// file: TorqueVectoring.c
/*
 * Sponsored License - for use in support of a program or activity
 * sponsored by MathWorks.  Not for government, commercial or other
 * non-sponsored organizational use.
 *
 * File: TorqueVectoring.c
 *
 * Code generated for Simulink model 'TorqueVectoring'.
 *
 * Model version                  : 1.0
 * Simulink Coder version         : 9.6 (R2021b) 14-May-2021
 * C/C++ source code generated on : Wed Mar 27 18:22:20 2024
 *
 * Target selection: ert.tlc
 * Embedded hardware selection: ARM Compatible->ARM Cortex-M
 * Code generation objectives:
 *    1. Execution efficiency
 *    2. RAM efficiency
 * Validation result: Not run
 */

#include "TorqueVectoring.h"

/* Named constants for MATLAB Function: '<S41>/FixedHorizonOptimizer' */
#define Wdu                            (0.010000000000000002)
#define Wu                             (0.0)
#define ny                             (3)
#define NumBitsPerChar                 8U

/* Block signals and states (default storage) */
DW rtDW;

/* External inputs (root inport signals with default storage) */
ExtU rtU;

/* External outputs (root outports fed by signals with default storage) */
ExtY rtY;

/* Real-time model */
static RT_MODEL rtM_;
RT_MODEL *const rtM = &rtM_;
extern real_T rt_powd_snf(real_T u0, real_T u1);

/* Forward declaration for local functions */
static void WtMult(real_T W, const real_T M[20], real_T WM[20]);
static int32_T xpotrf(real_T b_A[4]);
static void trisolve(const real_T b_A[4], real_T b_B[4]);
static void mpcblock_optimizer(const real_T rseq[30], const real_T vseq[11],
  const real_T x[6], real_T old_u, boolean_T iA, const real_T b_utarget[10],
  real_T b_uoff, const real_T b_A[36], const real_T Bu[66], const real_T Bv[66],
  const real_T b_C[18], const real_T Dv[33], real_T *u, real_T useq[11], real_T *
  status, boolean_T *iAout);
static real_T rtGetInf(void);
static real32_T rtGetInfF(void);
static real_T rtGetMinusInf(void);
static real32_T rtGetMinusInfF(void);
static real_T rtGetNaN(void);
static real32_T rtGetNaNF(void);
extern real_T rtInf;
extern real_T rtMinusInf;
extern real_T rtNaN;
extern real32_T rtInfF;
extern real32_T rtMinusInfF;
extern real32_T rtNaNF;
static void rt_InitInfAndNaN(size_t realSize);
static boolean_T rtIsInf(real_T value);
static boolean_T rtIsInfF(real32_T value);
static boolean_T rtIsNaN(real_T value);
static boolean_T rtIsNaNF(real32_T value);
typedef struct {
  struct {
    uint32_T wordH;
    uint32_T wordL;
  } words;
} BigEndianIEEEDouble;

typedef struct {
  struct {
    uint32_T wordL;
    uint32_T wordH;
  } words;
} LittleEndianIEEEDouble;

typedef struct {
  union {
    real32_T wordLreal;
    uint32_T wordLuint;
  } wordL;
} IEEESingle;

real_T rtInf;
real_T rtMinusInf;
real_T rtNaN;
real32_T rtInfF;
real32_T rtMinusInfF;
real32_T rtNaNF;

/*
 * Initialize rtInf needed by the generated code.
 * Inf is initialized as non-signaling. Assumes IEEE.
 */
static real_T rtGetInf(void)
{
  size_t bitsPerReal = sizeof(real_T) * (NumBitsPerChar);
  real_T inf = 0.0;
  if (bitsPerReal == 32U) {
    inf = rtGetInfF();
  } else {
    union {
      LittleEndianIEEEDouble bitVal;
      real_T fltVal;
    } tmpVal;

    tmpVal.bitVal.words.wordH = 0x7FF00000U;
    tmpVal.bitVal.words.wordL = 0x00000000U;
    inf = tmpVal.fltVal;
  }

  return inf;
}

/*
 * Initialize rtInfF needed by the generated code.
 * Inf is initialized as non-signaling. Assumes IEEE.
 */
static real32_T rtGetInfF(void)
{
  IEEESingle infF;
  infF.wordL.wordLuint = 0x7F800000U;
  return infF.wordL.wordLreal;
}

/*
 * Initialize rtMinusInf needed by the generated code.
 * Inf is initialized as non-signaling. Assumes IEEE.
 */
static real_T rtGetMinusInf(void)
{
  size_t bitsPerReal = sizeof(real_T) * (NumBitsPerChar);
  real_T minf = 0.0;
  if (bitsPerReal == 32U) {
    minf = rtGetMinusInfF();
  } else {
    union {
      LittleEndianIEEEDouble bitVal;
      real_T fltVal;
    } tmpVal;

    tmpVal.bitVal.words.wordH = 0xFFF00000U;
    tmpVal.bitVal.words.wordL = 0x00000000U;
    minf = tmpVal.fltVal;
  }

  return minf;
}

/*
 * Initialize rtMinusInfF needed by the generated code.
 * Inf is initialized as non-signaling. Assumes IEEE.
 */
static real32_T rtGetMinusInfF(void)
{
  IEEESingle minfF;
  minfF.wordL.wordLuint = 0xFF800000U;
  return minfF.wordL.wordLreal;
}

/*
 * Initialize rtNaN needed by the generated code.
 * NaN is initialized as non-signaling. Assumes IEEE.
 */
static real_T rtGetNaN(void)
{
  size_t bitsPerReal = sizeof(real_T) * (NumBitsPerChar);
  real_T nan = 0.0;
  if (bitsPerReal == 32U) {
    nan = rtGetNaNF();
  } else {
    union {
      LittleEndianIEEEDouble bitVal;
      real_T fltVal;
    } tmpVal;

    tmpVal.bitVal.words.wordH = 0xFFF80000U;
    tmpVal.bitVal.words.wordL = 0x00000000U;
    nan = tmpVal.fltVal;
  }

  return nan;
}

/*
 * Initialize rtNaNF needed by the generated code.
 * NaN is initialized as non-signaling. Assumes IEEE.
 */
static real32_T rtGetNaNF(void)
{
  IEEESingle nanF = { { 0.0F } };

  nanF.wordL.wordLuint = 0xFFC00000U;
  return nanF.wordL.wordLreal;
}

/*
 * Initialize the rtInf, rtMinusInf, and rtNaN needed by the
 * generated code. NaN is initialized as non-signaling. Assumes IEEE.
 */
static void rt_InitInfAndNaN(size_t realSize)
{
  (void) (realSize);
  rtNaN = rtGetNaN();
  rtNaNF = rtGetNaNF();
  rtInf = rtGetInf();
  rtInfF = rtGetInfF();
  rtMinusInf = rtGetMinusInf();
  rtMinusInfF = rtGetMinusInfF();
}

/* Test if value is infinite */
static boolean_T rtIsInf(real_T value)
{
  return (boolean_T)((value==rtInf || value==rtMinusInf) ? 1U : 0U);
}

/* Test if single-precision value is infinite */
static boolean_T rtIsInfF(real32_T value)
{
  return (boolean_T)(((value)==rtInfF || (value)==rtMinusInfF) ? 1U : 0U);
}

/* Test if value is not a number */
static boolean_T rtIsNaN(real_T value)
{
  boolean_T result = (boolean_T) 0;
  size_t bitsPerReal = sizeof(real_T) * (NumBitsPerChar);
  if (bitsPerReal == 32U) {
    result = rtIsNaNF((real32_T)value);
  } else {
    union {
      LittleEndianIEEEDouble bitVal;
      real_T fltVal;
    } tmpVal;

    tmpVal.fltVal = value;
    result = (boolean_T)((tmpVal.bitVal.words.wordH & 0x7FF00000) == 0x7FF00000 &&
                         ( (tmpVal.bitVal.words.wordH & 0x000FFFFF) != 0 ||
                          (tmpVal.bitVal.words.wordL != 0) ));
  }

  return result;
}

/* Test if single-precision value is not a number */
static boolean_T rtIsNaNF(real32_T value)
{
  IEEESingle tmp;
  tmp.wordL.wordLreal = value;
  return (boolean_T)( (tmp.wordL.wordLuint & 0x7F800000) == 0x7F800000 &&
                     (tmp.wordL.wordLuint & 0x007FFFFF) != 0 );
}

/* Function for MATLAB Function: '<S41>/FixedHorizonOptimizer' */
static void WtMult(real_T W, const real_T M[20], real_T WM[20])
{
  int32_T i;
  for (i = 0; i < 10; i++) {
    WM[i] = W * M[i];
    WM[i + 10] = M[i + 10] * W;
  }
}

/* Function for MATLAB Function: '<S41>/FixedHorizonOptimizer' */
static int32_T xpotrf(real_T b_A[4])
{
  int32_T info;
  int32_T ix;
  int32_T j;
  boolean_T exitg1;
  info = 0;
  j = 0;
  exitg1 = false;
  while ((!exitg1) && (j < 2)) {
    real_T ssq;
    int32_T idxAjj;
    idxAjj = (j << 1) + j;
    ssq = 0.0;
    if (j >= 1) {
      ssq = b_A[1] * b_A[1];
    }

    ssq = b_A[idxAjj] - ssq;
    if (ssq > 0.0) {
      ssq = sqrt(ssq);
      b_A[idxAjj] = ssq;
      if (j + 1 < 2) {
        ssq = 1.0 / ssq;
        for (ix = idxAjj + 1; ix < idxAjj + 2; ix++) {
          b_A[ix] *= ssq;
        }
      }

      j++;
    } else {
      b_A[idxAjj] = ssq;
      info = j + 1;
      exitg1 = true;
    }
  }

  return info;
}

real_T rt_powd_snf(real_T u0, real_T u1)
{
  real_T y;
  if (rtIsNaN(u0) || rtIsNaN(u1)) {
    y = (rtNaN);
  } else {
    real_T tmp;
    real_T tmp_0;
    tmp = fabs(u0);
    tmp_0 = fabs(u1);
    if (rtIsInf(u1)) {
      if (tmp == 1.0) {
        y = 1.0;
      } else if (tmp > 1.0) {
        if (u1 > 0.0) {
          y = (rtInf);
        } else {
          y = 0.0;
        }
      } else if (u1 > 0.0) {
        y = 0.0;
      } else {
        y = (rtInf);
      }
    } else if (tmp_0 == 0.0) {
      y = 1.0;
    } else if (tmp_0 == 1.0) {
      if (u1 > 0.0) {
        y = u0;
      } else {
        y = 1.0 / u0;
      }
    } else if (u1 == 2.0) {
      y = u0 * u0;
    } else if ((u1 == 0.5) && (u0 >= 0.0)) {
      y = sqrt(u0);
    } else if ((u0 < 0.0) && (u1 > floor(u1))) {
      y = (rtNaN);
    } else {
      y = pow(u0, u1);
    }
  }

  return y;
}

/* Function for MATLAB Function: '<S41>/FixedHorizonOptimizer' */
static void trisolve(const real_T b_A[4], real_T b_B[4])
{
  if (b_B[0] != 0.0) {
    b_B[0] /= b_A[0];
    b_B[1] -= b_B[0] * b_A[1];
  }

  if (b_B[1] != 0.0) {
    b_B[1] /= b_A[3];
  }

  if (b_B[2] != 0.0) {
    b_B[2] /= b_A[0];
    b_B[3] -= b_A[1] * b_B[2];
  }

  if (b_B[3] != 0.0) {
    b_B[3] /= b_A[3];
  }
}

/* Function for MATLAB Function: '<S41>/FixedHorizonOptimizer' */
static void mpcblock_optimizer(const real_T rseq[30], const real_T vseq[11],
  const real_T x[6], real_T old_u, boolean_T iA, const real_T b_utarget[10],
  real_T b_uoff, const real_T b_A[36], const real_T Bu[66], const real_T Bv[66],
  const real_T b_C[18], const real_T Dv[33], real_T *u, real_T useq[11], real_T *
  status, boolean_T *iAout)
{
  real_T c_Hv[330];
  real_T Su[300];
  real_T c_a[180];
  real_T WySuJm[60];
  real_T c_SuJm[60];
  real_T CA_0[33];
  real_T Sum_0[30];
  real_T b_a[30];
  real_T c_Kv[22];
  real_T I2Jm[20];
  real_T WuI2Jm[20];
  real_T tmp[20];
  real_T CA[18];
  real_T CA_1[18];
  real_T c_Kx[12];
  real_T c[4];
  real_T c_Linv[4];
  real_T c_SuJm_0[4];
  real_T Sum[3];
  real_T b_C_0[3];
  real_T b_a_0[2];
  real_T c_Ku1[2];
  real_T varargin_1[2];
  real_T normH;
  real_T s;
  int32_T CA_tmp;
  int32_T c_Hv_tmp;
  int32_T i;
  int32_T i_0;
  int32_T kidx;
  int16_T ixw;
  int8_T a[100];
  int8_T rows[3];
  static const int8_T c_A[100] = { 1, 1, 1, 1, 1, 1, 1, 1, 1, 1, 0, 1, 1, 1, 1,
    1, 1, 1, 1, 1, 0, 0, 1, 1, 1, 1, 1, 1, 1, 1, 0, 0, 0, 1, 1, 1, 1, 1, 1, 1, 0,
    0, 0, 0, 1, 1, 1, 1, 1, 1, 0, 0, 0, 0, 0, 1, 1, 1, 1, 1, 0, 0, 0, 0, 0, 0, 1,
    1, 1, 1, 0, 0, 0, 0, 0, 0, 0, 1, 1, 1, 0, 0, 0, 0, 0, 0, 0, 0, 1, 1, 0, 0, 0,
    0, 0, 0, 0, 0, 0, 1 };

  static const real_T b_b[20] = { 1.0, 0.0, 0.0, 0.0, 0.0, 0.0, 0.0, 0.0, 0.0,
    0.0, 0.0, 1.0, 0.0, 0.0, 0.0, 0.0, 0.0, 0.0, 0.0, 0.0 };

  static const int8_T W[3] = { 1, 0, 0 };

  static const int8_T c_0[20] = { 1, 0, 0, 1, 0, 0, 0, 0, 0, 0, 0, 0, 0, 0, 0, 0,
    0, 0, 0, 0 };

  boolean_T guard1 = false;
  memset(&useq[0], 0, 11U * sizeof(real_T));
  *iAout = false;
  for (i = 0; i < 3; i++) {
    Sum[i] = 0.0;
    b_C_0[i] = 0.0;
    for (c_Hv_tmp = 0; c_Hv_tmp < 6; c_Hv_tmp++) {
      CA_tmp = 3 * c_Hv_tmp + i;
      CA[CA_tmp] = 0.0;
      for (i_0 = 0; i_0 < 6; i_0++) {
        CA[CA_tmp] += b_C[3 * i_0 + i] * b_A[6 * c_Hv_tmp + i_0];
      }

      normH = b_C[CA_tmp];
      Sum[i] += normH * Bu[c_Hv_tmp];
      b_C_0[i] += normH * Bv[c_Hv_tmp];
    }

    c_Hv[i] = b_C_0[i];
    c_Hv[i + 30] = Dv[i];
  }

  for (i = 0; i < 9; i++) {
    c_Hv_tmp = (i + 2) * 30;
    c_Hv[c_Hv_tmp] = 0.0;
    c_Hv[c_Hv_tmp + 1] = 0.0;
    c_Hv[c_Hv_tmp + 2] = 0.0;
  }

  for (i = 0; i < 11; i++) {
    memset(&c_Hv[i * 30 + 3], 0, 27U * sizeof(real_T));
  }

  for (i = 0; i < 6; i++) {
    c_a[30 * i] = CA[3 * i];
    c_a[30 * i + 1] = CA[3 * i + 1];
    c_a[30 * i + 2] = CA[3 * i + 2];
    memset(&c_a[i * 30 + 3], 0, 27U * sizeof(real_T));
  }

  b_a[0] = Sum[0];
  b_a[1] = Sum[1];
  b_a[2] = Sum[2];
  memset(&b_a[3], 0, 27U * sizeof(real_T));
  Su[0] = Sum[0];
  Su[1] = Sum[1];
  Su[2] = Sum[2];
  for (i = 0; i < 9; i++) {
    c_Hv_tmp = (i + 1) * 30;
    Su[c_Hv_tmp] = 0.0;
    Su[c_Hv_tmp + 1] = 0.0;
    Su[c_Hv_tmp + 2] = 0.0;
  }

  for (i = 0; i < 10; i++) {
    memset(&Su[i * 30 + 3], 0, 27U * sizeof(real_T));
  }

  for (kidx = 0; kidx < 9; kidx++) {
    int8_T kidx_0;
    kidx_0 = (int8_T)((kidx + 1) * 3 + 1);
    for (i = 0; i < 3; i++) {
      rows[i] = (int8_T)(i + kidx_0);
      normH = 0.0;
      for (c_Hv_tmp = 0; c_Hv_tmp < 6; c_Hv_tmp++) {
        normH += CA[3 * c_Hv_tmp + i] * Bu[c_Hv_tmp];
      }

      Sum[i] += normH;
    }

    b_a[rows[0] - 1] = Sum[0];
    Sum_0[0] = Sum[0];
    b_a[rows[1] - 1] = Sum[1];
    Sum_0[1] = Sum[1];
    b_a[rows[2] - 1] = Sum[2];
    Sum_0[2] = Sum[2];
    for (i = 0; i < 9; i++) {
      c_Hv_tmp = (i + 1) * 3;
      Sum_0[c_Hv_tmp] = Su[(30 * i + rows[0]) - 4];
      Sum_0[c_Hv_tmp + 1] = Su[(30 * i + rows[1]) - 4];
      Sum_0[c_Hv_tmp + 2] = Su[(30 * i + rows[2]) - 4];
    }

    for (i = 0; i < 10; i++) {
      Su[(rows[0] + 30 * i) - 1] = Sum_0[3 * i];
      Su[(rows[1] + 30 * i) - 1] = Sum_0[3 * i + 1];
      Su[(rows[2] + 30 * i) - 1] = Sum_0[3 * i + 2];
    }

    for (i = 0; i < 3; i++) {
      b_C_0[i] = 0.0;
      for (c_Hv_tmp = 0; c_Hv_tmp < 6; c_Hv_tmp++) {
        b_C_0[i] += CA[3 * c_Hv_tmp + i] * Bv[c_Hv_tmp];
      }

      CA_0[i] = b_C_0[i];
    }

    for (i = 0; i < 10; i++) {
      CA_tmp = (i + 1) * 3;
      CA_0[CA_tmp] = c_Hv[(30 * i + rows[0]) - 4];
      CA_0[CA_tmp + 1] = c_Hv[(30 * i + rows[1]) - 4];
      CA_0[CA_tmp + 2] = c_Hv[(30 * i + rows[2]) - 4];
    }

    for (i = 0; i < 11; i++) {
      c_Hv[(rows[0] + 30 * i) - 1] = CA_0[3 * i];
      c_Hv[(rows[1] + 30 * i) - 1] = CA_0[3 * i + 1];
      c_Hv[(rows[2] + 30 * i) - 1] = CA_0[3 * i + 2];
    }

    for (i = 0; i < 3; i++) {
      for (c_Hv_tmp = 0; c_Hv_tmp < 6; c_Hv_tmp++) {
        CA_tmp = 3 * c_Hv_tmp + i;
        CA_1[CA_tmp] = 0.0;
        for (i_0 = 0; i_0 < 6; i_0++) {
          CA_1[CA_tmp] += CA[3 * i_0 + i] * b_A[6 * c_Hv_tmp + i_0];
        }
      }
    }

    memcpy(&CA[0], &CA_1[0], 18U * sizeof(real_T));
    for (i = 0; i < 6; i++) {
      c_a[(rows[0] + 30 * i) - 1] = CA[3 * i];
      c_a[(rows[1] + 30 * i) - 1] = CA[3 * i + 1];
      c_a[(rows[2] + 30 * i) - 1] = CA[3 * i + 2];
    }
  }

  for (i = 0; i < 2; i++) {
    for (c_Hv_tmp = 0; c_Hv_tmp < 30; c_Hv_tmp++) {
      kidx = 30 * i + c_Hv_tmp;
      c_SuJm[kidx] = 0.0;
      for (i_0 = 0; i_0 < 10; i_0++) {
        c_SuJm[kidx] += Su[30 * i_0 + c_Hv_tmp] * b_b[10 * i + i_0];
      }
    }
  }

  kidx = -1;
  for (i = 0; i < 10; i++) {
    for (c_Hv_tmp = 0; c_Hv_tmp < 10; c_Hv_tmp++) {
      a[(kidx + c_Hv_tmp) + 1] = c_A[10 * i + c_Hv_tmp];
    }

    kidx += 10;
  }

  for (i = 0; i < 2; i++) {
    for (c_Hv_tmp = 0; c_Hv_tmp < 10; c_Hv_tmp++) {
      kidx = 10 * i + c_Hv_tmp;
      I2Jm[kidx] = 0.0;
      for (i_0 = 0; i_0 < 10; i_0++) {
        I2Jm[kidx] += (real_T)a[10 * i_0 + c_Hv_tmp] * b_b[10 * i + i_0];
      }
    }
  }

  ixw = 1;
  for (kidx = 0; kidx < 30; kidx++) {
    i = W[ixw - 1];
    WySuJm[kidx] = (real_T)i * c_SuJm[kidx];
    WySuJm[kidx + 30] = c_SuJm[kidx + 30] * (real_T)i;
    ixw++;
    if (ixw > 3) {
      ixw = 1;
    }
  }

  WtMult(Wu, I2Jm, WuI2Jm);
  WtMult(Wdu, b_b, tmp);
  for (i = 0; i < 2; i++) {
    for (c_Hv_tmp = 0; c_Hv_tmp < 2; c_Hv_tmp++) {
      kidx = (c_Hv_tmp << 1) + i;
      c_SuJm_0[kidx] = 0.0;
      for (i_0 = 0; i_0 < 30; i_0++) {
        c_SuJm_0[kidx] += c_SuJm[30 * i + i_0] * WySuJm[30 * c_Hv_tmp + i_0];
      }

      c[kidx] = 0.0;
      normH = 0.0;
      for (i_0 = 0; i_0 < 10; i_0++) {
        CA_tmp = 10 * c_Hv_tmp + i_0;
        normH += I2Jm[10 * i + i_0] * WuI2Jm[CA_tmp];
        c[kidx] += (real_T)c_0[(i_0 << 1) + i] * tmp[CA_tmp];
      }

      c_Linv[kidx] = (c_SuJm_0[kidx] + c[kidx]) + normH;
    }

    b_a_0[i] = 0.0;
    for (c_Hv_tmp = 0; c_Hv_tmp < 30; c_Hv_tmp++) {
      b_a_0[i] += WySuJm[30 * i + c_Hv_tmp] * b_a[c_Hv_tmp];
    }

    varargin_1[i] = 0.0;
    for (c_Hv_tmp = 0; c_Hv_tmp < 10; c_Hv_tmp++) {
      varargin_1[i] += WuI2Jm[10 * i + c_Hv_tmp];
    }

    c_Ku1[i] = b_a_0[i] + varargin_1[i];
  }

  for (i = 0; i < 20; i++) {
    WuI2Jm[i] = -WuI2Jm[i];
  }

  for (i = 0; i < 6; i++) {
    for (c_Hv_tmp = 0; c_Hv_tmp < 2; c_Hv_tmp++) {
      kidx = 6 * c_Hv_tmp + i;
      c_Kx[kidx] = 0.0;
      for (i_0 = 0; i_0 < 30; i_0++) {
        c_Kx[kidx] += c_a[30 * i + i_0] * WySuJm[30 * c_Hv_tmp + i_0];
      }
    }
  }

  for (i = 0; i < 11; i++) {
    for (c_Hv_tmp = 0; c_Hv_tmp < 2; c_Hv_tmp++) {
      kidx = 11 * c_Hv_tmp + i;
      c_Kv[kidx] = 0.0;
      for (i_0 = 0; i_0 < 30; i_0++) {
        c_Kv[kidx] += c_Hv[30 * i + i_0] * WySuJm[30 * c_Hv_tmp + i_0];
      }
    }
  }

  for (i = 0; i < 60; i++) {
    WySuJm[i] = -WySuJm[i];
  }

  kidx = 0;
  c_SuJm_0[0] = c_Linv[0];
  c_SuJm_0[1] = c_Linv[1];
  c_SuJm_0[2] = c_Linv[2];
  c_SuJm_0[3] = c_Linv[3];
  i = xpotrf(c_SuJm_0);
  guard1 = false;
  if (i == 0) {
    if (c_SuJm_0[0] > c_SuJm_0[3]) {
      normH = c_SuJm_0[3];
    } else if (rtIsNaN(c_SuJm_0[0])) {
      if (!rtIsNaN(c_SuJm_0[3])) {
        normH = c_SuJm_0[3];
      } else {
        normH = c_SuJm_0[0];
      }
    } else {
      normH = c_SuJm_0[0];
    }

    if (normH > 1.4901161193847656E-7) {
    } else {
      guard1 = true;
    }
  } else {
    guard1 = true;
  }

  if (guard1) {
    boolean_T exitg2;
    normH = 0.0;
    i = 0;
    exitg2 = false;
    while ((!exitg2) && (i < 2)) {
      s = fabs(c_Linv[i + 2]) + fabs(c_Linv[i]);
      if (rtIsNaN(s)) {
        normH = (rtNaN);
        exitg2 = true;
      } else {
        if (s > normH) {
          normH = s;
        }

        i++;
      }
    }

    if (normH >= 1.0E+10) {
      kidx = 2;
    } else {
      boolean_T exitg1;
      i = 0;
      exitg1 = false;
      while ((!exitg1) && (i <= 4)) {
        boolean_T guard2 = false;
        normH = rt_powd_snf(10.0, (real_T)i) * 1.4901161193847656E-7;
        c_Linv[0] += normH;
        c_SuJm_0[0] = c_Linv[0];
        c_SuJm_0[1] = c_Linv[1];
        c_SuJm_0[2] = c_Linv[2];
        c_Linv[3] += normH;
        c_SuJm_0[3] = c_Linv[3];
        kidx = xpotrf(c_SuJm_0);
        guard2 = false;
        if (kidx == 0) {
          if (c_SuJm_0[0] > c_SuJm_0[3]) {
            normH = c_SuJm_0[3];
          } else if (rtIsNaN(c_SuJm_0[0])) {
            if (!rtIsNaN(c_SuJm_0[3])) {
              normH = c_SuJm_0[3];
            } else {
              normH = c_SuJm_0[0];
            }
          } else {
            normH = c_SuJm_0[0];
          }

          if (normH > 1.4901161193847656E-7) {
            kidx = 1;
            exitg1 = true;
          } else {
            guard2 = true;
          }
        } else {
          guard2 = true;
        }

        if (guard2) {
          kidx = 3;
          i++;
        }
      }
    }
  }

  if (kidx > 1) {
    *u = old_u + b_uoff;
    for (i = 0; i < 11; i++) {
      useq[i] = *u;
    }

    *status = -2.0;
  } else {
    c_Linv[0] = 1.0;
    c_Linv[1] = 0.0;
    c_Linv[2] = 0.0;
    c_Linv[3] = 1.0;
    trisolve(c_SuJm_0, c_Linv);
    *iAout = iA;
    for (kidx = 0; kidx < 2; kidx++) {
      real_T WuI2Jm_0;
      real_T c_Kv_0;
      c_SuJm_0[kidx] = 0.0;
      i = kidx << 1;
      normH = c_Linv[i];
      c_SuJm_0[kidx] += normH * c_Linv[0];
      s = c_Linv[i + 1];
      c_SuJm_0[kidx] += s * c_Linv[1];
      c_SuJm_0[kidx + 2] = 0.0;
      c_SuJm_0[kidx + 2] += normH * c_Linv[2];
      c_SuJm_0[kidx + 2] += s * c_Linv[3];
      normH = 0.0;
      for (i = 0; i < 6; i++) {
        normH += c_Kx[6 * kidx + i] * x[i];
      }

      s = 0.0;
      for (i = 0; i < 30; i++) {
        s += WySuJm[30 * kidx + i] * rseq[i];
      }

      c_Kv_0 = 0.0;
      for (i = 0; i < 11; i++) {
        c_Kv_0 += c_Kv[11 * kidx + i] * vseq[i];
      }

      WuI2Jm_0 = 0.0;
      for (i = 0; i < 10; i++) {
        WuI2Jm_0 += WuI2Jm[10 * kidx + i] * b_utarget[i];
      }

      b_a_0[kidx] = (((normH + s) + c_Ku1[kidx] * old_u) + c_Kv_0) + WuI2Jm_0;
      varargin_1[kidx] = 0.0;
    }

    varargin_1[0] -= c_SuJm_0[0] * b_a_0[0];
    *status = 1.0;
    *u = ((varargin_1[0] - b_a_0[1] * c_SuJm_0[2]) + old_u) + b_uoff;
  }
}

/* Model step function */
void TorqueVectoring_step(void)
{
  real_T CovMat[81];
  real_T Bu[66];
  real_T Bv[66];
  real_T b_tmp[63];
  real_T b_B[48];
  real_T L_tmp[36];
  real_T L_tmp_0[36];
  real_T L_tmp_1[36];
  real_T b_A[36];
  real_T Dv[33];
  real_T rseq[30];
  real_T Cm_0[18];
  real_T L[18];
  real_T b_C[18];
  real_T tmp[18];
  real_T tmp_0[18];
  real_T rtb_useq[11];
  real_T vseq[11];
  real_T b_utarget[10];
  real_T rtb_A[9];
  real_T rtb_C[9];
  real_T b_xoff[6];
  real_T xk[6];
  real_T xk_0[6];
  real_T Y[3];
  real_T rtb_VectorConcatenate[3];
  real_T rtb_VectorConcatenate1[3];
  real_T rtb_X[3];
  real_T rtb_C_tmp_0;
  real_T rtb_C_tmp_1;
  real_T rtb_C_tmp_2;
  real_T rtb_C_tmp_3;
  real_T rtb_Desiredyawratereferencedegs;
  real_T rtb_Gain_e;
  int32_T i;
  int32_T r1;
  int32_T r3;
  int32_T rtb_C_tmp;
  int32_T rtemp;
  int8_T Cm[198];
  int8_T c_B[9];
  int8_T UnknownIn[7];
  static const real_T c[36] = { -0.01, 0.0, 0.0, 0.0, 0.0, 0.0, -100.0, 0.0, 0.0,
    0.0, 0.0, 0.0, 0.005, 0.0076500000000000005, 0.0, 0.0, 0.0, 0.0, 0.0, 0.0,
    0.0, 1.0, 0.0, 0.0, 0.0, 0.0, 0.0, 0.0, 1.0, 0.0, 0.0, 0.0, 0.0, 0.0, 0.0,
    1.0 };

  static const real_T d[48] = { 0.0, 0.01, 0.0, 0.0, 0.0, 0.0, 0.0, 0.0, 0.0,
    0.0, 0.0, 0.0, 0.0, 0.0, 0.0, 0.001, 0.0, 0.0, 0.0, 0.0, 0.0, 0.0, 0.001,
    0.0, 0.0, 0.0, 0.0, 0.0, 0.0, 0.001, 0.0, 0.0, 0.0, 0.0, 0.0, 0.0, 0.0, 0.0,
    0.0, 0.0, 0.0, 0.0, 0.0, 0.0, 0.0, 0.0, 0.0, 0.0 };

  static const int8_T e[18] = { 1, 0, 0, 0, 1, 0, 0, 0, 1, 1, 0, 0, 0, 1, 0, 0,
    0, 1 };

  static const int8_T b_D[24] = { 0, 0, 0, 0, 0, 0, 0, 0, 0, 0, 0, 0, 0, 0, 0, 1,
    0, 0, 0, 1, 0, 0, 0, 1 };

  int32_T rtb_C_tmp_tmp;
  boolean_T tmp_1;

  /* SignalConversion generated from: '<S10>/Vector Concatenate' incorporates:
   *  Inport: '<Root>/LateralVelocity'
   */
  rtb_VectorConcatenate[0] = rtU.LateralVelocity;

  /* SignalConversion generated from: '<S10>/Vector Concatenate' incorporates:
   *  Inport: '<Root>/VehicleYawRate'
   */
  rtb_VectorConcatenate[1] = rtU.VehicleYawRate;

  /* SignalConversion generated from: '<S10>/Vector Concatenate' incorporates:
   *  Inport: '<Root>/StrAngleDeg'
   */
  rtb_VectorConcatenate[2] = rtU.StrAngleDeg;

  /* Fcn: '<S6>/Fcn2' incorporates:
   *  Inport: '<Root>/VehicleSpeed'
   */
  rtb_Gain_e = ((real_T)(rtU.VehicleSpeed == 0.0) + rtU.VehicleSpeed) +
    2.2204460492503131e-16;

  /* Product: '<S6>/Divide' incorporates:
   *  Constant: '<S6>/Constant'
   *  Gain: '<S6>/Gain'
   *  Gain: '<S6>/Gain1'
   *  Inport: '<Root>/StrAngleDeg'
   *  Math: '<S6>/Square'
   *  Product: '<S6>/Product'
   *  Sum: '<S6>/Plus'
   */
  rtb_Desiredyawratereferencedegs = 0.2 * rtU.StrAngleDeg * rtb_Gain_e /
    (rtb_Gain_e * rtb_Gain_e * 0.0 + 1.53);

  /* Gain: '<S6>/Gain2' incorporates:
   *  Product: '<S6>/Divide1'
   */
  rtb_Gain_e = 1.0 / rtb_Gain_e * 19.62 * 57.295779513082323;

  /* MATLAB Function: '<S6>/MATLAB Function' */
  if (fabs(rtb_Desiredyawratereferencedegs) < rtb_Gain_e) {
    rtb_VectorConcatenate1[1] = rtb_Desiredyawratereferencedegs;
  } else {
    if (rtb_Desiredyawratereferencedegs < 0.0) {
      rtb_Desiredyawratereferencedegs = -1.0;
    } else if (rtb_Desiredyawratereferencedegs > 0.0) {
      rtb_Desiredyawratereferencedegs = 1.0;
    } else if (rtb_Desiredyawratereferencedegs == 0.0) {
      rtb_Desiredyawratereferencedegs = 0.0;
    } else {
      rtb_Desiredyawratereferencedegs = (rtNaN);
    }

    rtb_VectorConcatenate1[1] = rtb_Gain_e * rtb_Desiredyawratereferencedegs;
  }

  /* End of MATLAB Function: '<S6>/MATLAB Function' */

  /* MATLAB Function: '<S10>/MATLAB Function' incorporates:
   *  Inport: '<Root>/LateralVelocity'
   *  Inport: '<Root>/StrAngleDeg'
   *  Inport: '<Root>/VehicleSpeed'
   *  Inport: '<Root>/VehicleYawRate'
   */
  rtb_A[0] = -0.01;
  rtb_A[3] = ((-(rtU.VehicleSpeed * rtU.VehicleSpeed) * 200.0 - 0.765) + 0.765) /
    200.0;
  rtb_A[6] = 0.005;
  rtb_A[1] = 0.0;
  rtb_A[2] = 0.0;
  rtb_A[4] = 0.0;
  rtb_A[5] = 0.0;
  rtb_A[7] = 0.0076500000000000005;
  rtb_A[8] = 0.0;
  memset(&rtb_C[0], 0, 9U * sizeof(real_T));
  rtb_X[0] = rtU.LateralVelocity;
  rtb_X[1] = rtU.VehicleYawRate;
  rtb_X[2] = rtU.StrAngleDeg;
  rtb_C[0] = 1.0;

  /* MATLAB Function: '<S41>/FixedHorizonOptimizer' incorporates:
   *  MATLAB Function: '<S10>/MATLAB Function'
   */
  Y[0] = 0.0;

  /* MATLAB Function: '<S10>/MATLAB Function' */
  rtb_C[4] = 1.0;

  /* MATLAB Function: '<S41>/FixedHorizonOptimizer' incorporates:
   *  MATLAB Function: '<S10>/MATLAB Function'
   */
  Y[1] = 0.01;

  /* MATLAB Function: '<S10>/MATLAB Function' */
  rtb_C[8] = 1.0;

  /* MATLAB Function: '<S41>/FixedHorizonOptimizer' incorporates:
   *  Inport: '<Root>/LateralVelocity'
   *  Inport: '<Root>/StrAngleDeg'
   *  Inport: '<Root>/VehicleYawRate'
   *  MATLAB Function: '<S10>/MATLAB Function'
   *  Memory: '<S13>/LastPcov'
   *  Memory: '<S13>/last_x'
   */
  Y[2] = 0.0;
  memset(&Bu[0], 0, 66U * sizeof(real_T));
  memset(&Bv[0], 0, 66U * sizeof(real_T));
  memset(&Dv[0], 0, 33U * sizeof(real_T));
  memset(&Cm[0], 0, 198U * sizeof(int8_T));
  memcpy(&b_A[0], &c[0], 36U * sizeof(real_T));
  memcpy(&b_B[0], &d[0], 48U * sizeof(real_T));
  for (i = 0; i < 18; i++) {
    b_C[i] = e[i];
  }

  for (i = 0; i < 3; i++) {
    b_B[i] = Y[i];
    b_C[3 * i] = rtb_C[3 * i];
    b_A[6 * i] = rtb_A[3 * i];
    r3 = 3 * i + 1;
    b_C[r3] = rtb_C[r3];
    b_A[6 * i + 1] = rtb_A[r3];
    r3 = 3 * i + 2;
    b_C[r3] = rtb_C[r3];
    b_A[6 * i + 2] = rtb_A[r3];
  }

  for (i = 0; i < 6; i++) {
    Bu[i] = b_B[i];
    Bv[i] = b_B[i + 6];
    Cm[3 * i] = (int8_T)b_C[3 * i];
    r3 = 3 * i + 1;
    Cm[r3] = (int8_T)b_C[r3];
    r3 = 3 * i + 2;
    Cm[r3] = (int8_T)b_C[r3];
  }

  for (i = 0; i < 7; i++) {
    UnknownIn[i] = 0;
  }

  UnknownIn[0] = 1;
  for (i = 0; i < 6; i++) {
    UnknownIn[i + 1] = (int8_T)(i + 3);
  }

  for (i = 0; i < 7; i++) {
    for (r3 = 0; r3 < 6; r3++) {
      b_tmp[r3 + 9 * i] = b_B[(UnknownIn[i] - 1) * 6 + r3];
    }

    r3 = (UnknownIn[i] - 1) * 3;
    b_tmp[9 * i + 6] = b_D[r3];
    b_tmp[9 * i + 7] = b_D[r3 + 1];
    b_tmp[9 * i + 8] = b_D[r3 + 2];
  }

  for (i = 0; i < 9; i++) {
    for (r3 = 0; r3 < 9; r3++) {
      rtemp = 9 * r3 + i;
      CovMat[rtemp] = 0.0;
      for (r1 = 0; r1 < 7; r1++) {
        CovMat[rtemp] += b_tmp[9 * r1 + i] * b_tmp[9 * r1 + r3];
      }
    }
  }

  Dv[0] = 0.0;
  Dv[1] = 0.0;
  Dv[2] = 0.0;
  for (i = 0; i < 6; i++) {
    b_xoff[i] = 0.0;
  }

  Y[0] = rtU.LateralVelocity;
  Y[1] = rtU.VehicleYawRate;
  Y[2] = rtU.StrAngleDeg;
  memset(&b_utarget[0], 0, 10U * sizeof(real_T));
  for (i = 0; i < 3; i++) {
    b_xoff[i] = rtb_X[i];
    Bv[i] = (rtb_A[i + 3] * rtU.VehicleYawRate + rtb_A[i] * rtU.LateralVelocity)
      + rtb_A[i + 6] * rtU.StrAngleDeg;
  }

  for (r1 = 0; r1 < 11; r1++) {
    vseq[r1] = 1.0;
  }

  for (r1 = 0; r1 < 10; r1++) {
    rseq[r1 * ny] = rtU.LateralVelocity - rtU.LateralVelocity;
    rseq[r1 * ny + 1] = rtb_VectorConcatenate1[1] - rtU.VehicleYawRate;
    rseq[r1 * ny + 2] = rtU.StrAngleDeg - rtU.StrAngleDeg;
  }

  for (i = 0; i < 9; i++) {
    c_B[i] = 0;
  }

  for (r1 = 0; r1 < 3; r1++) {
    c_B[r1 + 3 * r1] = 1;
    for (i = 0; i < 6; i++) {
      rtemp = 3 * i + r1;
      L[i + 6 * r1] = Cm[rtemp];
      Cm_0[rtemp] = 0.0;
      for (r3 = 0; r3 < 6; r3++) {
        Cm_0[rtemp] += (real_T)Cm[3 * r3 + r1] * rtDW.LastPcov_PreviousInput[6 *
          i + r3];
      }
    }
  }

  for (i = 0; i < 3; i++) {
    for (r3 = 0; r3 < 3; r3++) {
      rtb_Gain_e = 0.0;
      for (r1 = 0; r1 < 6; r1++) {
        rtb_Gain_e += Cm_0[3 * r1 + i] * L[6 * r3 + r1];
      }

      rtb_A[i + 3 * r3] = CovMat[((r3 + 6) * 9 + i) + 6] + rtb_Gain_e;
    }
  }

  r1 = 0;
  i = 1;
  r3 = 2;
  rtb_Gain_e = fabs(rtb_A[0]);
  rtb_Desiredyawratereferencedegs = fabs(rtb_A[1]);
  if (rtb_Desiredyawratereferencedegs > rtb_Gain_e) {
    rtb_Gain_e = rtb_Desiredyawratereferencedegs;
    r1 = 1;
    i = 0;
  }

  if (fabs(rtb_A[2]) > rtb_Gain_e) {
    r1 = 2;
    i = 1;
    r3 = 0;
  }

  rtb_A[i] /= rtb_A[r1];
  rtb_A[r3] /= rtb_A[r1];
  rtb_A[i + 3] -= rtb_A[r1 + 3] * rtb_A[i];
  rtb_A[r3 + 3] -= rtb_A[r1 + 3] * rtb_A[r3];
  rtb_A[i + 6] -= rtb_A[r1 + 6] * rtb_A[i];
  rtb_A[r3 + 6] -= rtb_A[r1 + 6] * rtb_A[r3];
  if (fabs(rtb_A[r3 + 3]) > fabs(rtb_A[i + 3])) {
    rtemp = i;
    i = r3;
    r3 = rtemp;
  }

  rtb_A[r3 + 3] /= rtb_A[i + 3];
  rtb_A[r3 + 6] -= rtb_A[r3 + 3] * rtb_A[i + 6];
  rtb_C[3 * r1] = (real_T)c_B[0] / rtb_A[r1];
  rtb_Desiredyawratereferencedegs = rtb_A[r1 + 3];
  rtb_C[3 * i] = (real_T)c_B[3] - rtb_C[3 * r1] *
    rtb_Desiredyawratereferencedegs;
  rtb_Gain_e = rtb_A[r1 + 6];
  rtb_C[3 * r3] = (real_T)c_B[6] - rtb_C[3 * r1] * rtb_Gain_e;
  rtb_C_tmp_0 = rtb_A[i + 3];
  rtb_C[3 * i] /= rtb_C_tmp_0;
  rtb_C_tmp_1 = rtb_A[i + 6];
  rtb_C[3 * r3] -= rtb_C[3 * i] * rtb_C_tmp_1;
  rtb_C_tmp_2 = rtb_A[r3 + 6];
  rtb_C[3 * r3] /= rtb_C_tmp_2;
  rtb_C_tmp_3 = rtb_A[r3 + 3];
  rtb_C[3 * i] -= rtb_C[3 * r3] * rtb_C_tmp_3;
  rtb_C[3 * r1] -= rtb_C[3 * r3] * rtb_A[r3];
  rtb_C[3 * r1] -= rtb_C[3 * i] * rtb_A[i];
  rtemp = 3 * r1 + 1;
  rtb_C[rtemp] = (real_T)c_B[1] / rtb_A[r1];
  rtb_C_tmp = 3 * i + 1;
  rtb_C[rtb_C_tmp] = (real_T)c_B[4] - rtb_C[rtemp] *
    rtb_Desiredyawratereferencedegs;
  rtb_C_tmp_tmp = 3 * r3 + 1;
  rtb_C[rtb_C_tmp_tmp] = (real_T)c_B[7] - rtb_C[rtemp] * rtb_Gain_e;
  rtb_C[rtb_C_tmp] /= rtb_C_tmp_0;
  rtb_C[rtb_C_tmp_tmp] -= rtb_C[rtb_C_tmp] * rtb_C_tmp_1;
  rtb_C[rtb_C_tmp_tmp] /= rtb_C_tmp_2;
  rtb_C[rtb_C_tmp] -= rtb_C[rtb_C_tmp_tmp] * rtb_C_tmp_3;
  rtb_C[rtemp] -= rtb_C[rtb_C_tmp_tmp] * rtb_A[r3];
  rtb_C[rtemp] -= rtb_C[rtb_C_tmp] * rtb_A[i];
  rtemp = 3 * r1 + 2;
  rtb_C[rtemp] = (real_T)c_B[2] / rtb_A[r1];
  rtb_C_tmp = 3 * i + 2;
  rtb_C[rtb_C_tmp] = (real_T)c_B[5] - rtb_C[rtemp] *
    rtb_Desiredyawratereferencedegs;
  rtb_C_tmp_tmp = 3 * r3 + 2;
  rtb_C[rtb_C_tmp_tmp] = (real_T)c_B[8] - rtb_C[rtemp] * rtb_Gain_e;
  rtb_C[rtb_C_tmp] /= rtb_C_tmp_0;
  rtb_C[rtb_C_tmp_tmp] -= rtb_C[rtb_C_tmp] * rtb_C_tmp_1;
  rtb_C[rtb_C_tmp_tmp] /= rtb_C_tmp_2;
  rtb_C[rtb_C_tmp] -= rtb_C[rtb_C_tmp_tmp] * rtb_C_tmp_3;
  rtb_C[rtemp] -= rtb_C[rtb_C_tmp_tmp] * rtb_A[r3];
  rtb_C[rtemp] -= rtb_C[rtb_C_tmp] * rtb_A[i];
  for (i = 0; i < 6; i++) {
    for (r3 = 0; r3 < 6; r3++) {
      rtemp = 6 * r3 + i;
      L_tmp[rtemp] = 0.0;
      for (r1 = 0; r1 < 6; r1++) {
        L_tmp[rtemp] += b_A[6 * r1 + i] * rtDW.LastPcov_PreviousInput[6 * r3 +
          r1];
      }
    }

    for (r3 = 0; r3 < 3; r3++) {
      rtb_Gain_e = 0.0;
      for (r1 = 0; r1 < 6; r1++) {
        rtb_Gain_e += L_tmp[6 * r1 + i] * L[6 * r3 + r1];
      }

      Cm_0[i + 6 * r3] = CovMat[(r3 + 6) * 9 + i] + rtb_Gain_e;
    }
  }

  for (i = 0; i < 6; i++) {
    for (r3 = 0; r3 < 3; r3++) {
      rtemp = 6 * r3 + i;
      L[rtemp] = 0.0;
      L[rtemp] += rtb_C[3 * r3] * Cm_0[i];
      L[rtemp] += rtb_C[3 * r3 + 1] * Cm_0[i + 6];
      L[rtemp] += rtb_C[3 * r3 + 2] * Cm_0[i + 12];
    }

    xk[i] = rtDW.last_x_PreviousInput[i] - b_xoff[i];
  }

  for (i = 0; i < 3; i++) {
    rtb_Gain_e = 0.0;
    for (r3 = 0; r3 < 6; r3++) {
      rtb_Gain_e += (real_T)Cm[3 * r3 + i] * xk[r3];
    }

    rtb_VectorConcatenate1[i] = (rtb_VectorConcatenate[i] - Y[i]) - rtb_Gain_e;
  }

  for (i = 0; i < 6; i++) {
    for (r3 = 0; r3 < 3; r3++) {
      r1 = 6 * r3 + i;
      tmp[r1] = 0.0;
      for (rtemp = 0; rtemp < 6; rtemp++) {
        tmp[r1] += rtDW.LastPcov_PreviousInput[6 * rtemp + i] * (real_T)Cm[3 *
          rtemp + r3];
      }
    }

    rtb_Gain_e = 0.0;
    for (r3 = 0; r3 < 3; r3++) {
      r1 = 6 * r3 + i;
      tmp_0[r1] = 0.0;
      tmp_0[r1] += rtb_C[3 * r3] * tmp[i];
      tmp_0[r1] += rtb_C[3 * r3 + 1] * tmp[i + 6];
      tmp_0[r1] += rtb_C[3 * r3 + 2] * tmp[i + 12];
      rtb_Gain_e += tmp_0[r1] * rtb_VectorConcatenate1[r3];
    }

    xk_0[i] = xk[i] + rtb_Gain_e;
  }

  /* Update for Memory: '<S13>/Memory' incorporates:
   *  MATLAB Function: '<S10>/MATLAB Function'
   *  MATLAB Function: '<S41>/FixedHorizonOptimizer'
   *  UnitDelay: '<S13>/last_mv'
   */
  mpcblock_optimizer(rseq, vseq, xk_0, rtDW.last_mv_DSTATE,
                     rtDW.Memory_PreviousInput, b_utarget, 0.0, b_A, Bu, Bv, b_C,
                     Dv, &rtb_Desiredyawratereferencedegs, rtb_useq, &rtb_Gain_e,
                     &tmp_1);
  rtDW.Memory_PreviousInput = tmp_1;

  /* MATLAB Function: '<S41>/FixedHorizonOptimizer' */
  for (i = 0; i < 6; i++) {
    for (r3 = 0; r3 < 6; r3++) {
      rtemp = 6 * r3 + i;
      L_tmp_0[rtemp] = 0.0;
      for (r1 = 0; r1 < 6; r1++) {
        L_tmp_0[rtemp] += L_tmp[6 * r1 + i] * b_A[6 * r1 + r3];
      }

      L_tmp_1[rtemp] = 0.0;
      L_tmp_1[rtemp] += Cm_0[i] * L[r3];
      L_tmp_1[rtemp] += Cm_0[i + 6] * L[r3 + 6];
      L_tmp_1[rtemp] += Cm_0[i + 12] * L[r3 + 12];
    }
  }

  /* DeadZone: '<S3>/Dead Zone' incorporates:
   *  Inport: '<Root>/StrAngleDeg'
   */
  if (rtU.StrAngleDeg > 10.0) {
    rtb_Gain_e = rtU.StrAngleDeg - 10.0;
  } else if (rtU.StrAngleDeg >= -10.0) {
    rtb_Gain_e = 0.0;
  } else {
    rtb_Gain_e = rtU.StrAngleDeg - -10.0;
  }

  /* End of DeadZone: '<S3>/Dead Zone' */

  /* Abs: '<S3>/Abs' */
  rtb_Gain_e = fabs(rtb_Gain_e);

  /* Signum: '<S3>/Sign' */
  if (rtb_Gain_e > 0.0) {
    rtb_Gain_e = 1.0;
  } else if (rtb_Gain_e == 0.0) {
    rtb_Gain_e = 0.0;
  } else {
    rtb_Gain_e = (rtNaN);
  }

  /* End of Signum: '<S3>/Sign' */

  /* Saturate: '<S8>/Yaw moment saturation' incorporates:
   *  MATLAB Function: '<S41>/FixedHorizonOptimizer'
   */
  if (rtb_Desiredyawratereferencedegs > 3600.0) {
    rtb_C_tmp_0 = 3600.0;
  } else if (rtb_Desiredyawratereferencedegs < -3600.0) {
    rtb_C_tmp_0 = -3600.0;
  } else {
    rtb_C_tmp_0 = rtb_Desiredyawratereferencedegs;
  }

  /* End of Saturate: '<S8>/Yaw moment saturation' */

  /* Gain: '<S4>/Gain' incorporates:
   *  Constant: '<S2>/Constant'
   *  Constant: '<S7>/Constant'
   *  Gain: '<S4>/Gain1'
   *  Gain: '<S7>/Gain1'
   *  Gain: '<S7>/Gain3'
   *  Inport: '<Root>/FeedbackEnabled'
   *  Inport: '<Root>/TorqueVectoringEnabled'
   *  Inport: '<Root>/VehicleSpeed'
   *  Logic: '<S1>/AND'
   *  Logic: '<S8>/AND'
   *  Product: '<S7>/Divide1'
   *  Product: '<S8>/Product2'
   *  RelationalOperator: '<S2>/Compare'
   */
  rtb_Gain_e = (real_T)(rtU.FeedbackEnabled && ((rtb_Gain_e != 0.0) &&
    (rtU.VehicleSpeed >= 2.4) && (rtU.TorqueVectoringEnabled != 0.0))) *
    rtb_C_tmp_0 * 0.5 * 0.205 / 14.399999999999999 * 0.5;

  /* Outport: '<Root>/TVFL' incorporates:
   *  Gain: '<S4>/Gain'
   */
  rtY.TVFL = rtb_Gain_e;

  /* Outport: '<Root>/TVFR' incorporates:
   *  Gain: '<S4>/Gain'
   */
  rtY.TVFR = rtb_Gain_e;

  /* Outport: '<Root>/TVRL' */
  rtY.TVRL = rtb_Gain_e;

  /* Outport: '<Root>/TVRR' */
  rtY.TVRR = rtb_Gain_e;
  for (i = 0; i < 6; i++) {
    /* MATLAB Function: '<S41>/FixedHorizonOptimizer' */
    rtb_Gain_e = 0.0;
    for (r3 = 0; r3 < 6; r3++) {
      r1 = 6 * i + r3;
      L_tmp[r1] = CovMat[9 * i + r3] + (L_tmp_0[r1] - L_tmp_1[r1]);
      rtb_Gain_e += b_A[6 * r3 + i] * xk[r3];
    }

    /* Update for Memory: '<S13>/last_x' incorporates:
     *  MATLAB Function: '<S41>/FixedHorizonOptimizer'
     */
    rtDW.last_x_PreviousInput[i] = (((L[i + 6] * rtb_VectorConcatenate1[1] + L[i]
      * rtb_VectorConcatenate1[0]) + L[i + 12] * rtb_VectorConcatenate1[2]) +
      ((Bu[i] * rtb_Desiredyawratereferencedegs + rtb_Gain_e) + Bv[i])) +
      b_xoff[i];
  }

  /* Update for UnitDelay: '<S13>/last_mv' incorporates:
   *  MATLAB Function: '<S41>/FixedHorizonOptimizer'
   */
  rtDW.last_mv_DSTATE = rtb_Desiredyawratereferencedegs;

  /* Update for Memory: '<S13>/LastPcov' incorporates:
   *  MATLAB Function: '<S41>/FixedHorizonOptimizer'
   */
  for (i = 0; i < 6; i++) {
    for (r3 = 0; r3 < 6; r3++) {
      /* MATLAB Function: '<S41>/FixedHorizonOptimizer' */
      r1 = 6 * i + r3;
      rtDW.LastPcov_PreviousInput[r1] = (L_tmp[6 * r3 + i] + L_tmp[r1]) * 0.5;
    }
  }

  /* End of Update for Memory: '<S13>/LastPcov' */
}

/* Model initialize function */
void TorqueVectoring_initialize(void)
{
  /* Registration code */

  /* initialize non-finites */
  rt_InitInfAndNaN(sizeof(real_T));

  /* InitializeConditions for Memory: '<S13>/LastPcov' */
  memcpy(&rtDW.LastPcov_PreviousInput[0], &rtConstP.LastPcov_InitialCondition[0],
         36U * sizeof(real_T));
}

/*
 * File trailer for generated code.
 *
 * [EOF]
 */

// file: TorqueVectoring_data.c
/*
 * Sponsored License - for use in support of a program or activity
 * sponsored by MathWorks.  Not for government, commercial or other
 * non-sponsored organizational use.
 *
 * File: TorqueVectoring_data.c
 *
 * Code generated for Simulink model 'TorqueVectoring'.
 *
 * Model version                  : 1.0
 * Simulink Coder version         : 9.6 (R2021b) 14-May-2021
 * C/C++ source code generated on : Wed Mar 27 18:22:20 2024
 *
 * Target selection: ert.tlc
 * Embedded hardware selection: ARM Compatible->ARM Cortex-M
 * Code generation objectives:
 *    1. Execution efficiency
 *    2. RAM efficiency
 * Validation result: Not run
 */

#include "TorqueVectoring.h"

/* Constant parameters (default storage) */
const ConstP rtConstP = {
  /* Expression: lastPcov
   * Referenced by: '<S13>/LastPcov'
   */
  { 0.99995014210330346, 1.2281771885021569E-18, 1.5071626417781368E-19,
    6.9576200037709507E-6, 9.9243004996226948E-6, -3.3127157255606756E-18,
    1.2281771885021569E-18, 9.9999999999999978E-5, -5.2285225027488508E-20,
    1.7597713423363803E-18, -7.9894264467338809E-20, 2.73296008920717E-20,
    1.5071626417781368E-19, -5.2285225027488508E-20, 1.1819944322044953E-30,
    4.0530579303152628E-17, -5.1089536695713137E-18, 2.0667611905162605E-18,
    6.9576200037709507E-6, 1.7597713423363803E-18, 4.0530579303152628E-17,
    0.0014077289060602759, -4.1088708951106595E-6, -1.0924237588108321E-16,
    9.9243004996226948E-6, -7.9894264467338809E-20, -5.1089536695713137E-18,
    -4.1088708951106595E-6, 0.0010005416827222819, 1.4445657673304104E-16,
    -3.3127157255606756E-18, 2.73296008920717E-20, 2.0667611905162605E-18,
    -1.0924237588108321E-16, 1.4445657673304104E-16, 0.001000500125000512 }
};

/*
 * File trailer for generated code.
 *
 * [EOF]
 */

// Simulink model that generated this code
simulink model "TorqueVectoring"  (R2021b)
settings: Solver=FixedStepDiscrete  StartTime=0.0  StopTime=10.0  FixedStep=0.001  RelTol=1e-3
model workspace (MAT data in the model file):
  DeadzoneYawrateError = 10
  SteeringDeadzonelimit = 10
values from neighbouring files (symbols this model uses):
  feedforwardgain = 4    [Controllerparameters.m]
  g = 9.81    [Controllerparameters.m]
  Gr = 12    [Controllerparameters.m]
  Ku = 0    [Controllerparameters.m]
  l = 1.53    [Controllerparameters.m]
  LowerYawMoment = -3600    [Controllerparameters.m]
  myy = 2    [Controllerparameters.m]
  Rd = 0.205    [Controllerparameters.m]
  Sgr = 5    [Controllerparameters.m]
  UpperYawMoment = 3600    [Controllerparameters.m]
  wf = 0.6    [Controllerparameters.m]
  wr = 0.6    [Controllerparameters.m]
libraries: simulink x1, mpclib x1

== system TorqueVectoring ==
  StrAngleDeg : Inport
  VehicleSpeed : Inport  Port=2
  TorqueVectoringEnabled : Inport  Port=3
  VehicleYawRate : Inport  Port=4
  FeedbackEnabled : Inport  Port=5
  FeedForwardEnabled : Inport  Port=6
  LateralVelocity : Inport  Port=7
  Subsystem : Subsystem
  TVFL : Outport
  TVFR : Outport  Port=2
  TVRL : Outport  Port=3
  TVRR : Outport  Port=4
  wires:
  Subsystem/3(TVRL) -> TVRL/1  "TV_torqueRL"
  Subsystem/4(TVRR) -> TVRR/1  "TV_torqueRR"
  Subsystem/1(TVFL) -> TVFL/1  "TV_torqueFL"
  StrAngleDeg/1 -> Subsystem/1(StrAngleDeg)
  VehicleSpeed/1 -> Subsystem/2(VehicleSpeed)
  TorqueVectoringEnabled/1 -> Subsystem/3(TorqueVectoringEnabled)
  FeedForwardEnabled/1 -> Subsystem/6(FeedForwardEnabled)
  FeedbackEnabled/1 -> Subsystem/5(FeedbackEnabled)
  VehicleYawRate/1 -> Subsystem/4(VehicleYawRate)
  Subsystem/2(TVFR) -> TVFR/1  "TV_torqueFR"
  LateralVelocity/1 -> Subsystem/7(LateralVelocity)

== system TorqueVectoring/Subsystem ==
  StrAngleDeg : Inport
  VehicleSpeed : Inport  Port=2
  TorqueVectoringEnabled : Inport  Port=3
  VehicleYawRate : Inport  Port=4
  FeedbackEnabled : Inport  Port=5
  FeedForwardEnabled : Inport  Port=6
  LateralVelocity : Inport  Port=7
  AND : Logic  Inputs=3  AllPortsSameDT=off  OutDataTypeStr=boolean
  Compare To Constant : simulink/Logic and Bit Operations/Compare To Constant  relop=>=  const=2.4  OutDataTypeStr=boolean
  "If steering angle is between -10 and 10 degrees system is off " : Subsystem
  StrAngleDeg1 : InportShadow
  StrAngleDeg2 : InportShadow
  VehicleSpeed1 : InportShadow  Port=2
  VehicleSpeed2 : InportShadow  Port=2
  Yaw moment distribution : Subsystem
  Yaw rate controller : Subsystem
  Yaw rate reference calculation : Subsystem
  TVFL : Outport
  TVFR : Outport  Port=2
  TVRL : Outport  Port=3
  TVRR : Outport  Port=4
  wires:
  VehicleSpeed2/1 -> Yaw rate controller/6(VehicleSpeed)
  StrAngleDeg1/1 -> Yaw rate reference calculation/1(StrAngleDeg)
  "If steering angle is between -10 and 10 degrees system is off "/1(logical 1 or 0) -> AND/1
  Yaw rate controller/1(Yaw moment) -> Yaw moment distribution/1(Yaw moment)
  VehicleSpeed/1 -> Compare To Constant/1
  StrAngleDeg/1 -> "If steering angle is between -10 and 10 degrees system is off "/1(Steering value)
  Yaw rate reference calculation/1(Yawratereference_data) -> Yaw rate controller/1(Yawratereference_data)
  AND/1 -> Yaw rate controller/2(TV_activation)  "TV activation"
  Compare To Constant/1 -> AND/2
  Yaw moment distribution/1(TV_torqueFL) -> TVFL/1  "TV_torqueFL"
  Yaw moment distribution/2(TV_torqueFR) -> TVFR/1  "TV_torqueFR"
  Yaw moment distribution/3(TV_torqueRL) -> TVRL/1  "TV_torqueRL"
  Yaw moment distribution/4(TV_torqueRR) -> TVRR/1  "TV_torqueRR"
  VehicleSpeed1/1 -> Yaw rate reference calculation/2(VehicleSpeed)
  VehicleYawRate/1 -> Yaw rate controller/5(VehicleYawRate)
  StrAngleDeg2/1 -> Yaw rate controller/3(StrAngleDeg)
  FeedbackEnabled/1 -> Yaw rate controller/4(FeedbackEnabled)
  FeedForwardEnabled/1 -> Yaw rate controller/7(FeedForwardEnabled)
  TorqueVectoringEnabled/1 -> AND/3
  LateralVelocity/1 -> Yaw rate controller/8(LateralVelocity)

== system TorqueVectoring/Subsystem/If steering angle is between -10 and 10 degrees system is off  ==
  Steering value : Inport
  Abs : Abs
  Dead Zone : DeadZone  LowerValue=-SteeringDeadzonelimit  UpperValue=SteeringDeadzonelimit  SaturateOnIntegerOverflow=on
  Sign : Signum
  logical 1 or 0 : Outport
  wires:
  Sign/1 -> logical 1 or 0/1
  Abs/1 -> Sign/1
  Dead Zone/1 -> Abs/1
  Steering value/1 -> Dead Zone/1

== system TorqueVectoring/Subsystem/Yaw moment distribution ==
  Yaw moment : Inport
  Gain : Gain  Gain=0.5
  Gain1 : Gain  Gain=0.5
  Lateral torque distribution : Subsystem
  TV_torqueFL : Outport
  TV_torqueFR : Outport  Port=2
  TV_torqueRL : Outport  Port=3
  TV_torqueRR : Outport  Port=4
  wires:
  Lateral torque distribution/2(TV_r) -> Gain1/1
  Lateral torque distribution/1(TV_f) -> Gain/1
  Gain/1 -> TV_torqueFL/1, TV_torqueFR/1
  Gain1/1 -> TV_torqueRR/1, TV_torqueRL/1
  Yaw moment/1 -> Lateral torque distribution/1(yaw moment)

== system TorqueVectoring/Subsystem/Yaw rate controller ==
  Yawratereference_data : Inport
  TV_activation : Inport  Port=2
  StrAngleDeg : Inport  Port=3
  FeedbackEnabled : Inport  Port=4
  VehicleYawRate : Inport  Port=5
  VehicleSpeed : Inport  Port=6
  FeedForwardEnabled : Inport  Port=7
  LateralVelocity : Inport  Port=8
  Feedback controller type : Subsystem
  Feedforward controller type : Subsystem
  Yaw moment saturation : Saturate  UpperLimit=UpperYawMoment  LowerLimit=LowerYawMoment
  Yaw moment : Outport
  wires:
  Yaw moment saturation/1 -> Yaw moment/1
  FeedbackEnabled/1 -> Feedback controller type/4(feedback)
  StrAngleDeg/1 -> Feedback controller type/6(SteeringAngle), Feedforward controller type/1("Steering wheel angle ")
  VehicleYawRate/1 -> Feedback controller type/3(Vehicle yaw rate rad/s)
  VehicleSpeed/1 -> Feedback controller type/2(Vehicle velocity m/s)
  TV_activation/1 -> Feedforward controller type/2(TV_activation), Feedback controller type/5(TV_activation)
  Yawratereference_data/1 -> Feedback controller type/1(Yawratereference_data)
  Feedforward controller type/1(Yawmomentfeedforward) -> ?
  Feedback controller type/1(Yawmomentfeedback) -> Yaw moment saturation/1
  FeedForwardEnabled/1 -> Feedforward controller type/3(FeedForwardEnabled)
  LateralVelocity/1 -> Feedback controller type/7(LateralVelocity)

== system TorqueVectoring/Subsystem/Yaw rate reference calculation ==
  StrAngleDeg : Inport
  VehicleSpeed : Inport  Port=2
  Constant : Constant  Value=l
  Constant1 : Constant  Value=myy
  Constant2 : Constant  Value=g
  Divide : Product  Inputs=*/
  Divide1 : Product  Inputs=/*
  Fcn2 : Fcn  Expr=u(1)+(u(1)==0)+eps
  Gain : Gain  Gain=Ku
  Gain1 : Gain  Gain=1/Sgr
  Gain2 : Gain  Gain=180/pi
  MATLAB Function : MATLAB Function  TreatAsAtomicUnit=on
  Plus : Sum
  Product : Product
  Product1 : Product
  Square : Math  Operator=square  SaturateOnIntegerOverflow=on
  Yawratereference_data : Outport
  wires:
  Fcn2/1 -> Square/1, Divide1/1, Product/2
  VehicleSpeed/1 -> Fcn2/1
  Divide1/1 -> Gain2/1  "Upper limit rad/s"
  Product1/1 -> Divide1/2
  Constant2/1 -> Product1/2
  Constant1/1 -> Product1/1
  Divide/1 -> MATLAB Function/1(yaw_rate_reference_original)  "Desired yaw rate reference deg/s"
  Gain1/1 -> Product/1  "Steering angle at wheels deg/s"
  Square/1 -> Gain/1
  Gain/1 -> Plus/2
  Constant/1 -> Plus/1
  Plus/1 -> Divide/2
  StrAngleDeg/1 -> Gain1/1
  Gain2/1 -> MATLAB Function/2(yaw_rate_limit)
  MATLAB Function/1(yaw_rate_reference) -> Yawratereference_data/1
  Product/1 -> Divide/1

== system TorqueVectoring/Subsystem/Yaw moment distribution/Lateral torque distribution ==
  yaw moment : Inport
  Constant : Constant  Value=2*wr*Gr
  Constant1 : Constant  Value=2*wf*Gr
  Divide1 : Product  Inputs=*/
  Divide2 : Product  Inputs=*/
  Gain : Gain  Gain=Rd
  Gain1 : Gain  Gain=Rd
  Gain2 : Gain  Gain=0.5
  Gain3 : Gain  Gain=0.5
  TV_f : Outport
  TV_r : Outport  Port=2
  wires:
  yaw moment/1 -> Gain2/1, Gain3/1
  Gain3/1 -> Gain1/1
  Gain2/1 -> Gain/1
  Gain1/1 -> Divide1/1
  Gain/1 -> Divide2/1
  Divide2/1 -> TV_r/1  "Desired torque difference at rear axle"
  Divide1/1 -> TV_f/1  "Desired torque difference at front axle"
  Constant1/1 -> Divide2/2
  Constant/1 -> Divide1/2

== system TorqueVectoring/Subsystem/Yaw rate controller/Feedback controller type ==
  Yawratereference_data : Inport
  Vehicle velocity m/s : Inport  Port=2
  Vehicle yaw rate rad/s : Inport  Port=3
  feedback : Inport  Port=4
  TV_activation : Inport  Port=5
  SteeringAngle : Inport  Port=6
  LateralVelocity : Inport  Port=7
  AND : Logic  AllPortsSameDT=off  OutDataTypeStr=boolean
  PI controller type : Subsystem
  Product2 : Product
  Yaw moment saturation : Saturate  UpperLimit=UpperYawMoment  LowerLimit=LowerYawMoment
  Yawmomentfeedback : Outport
  wires:
  Vehicle yaw rate rad/s/1 -> PI controller type/2(Vehicle yaw rate rad/s)
  Vehicle velocity m/s/1 -> PI controller type/1(Vehicle velocity m/s)
  feedback/1 -> AND/1
  PI controller type/1(Controller desired yaw moment1) -> Yaw moment saturation/1
  Yaw moment saturation/1 -> Product2/2
  Product2/1 -> Yawmomentfeedback/1
  AND/1 -> Product2/1
  TV_activation/1 -> AND/2
  Yawratereference_data/1 -> PI controller type/3(Vehicle yaw rate reference deg/s)
  SteeringAngle/1 -> PI controller type/4(SteeringAngle)
  LateralVelocity/1 -> PI controller type/5(LateralVelocity)

== system TorqueVectoring/Subsystem/Yaw rate controller/Feedforward controller type ==
  "Steering wheel angle " : Inport
  TV_activation : Inport  Port=2
  FeedForwardEnabled : Inport  Port=3
  AND : Logic  AllPortsSameDT=off  OutDataTypeStr=boolean
  Constant : Constant  Value=feedforwardgain
  Product : Product
  Product2 : Product
  Yaw moment saturation : Saturate  UpperLimit=UpperYawMoment  LowerLimit=LowerYawMoment
  Yawmomentfeedforward : Outport
  wires:
  "Steering wheel angle "/1 -> Product/1
  FeedForwardEnabled/1 -> AND/1
  TV_activation/1 -> AND/2
  AND/1 -> Product2/1
  Product/1 -> Yaw moment saturation/1
  Constant/1 -> Product/2
  Yaw moment saturation/1 -> Product2/2
  Product2/1 -> Yawmomentfeedforward/1

== system TorqueVectoring/Subsystem/Yaw rate controller/Feedback controller type/PI controller type ==
  Vehicle velocity m/s : Inport  PortDimensions=1
  Vehicle yaw rate rad/s : Inport  Port=2
  Vehicle yaw rate reference deg/s : Inport  Port=3
  SteeringAngle : Inport  Port=4
  LateralVelocity : Inport  Port=5
  Adaptive MPC Controller : mpclib/Adaptive MPC Controller  SCDEnableBlockLinearizationSpecification=on  mpcobj=mpc1  enable_value=0  updateMPCinCallerWorkspace=on  md_inport=off  mv_inport=off  uref_inport=off  return_cost=off  return_mvseq=off  return_qpstatus=off  return_xseq=off  return_state=off  return_ovseq=off  state_inport=off  isltv_plant=off  umin_inport=off  umax_inport=off  ymin_inport=off  ymax_inport=off  cc_inport=off  ywt_inport=off  uwt_inport=off  duwt_inport=off  rhoeps_inport=off  pm_inport=off  MaximumP=10  HorizonChoice=FixedHorizon  BlockDataType=double  SampleTimeInherited=off  switch_inport=off
  Bus Creator : BusCreator  Inputs=8
  MATLAB Function : MATLAB Function  TreatAsAtomicUnit=on
  NominalU1 : Bias  SaturateOnIntegerOverflow=on
  Scope : Scope
  Scope1 : Scope
  Vector Concatenate : Concatenate  NumInputs=3
  Vector Concatenate1 : Concatenate  NumInputs=3
  Controller desired yaw moment1 : Outport
  wires:
  Vehicle yaw rate reference deg/s/1 -> Vector Concatenate1/2
  Vehicle yaw rate rad/s/1 -> MATLAB Function/1(yr), Vector Concatenate/2
  Vector Concatenate/1 -> Adaptive MPC Controller/2
  LateralVelocity/1 -> MATLAB Function/3(v_y), Vector Concatenate1/1, Vector Concatenate/1  "Lateral velocity"
  SteeringAngle/1 -> MATLAB Function/2(str), Vector Concatenate1/3, Vector Concatenate/3
  Vector Concatenate1/1 -> Adaptive MPC Controller/3
  NominalU1/1 -> Scope1/1, Controller desired yaw moment1/1
  Adaptive MPC Controller/1 -> NominalU1/1
  MATLAB Function/1(A) -> Bus Creator/1
  MATLAB Function/2(B) -> Bus Creator/2
  MATLAB Function/3(C) -> Bus Creator/3
  MATLAB Function/4(D) -> Bus Creator/4
  MATLAB Function/5(U) -> Bus Creator/5
  MATLAB Function/6(Y) -> Bus Creator/6
  MATLAB Function/7(X) -> Bus Creator/7
  MATLAB Function/8(DX) -> Bus Creator/8
  Bus Creator/1 -> Adaptive MPC Controller/1
  Vehicle velocity m/s/1 -> MATLAB Function/4(v_x)

== matlab function TorqueVectoring/Subsystem/Yaw rate controller/Feedback controller type/PI controller type/MATLAB Function ==
function [A,B,C,D,U,Y,X,DX] = fcn(yr,str,v_y,v_x)

Cr = 1
Cf = 1
m = 200
Izz = 100
lf = 0.7650
lr = 0.7650

A = [-(Cr + Cf)/(m), (-v_x^2*m-Cf*lf + Cr*lr)/(m),Cf/m; (lr*Cr-lf*Cf)/(Izz), (lf^2*Cf-lr^2*Cr)/(Izz),lf*Cf/Izz;0,0,0];
B = [0; 1/Izz;0];
C = eye(3);
D = zeros([3,1]);
X = [v_y;yr;str];
Y = [v_y;yr;str];
U = [0];
%A= eye(3)+0.001*A;
%B=0.001*B;
%M=expm([A,B;zeros(1,4)]*0.001);
%A=M(1:3,1:3);
%B=M(1:3,4);
DX = A*X;

== matlab function TorqueVectoring/Subsystem/Yaw rate reference calculation/MATLAB Function ==
function yaw_rate_reference = fcn(yaw_rate_reference_original,yaw_rate_limit)

if abs(yaw_rate_reference_original) < yaw_rate_limit
    yaw_rate_reference = yaw_rate_reference_original ;
else 
    yaw_rate_reference = yaw_rate_limit*sign(yaw_rate_reference_original) ; 
end
